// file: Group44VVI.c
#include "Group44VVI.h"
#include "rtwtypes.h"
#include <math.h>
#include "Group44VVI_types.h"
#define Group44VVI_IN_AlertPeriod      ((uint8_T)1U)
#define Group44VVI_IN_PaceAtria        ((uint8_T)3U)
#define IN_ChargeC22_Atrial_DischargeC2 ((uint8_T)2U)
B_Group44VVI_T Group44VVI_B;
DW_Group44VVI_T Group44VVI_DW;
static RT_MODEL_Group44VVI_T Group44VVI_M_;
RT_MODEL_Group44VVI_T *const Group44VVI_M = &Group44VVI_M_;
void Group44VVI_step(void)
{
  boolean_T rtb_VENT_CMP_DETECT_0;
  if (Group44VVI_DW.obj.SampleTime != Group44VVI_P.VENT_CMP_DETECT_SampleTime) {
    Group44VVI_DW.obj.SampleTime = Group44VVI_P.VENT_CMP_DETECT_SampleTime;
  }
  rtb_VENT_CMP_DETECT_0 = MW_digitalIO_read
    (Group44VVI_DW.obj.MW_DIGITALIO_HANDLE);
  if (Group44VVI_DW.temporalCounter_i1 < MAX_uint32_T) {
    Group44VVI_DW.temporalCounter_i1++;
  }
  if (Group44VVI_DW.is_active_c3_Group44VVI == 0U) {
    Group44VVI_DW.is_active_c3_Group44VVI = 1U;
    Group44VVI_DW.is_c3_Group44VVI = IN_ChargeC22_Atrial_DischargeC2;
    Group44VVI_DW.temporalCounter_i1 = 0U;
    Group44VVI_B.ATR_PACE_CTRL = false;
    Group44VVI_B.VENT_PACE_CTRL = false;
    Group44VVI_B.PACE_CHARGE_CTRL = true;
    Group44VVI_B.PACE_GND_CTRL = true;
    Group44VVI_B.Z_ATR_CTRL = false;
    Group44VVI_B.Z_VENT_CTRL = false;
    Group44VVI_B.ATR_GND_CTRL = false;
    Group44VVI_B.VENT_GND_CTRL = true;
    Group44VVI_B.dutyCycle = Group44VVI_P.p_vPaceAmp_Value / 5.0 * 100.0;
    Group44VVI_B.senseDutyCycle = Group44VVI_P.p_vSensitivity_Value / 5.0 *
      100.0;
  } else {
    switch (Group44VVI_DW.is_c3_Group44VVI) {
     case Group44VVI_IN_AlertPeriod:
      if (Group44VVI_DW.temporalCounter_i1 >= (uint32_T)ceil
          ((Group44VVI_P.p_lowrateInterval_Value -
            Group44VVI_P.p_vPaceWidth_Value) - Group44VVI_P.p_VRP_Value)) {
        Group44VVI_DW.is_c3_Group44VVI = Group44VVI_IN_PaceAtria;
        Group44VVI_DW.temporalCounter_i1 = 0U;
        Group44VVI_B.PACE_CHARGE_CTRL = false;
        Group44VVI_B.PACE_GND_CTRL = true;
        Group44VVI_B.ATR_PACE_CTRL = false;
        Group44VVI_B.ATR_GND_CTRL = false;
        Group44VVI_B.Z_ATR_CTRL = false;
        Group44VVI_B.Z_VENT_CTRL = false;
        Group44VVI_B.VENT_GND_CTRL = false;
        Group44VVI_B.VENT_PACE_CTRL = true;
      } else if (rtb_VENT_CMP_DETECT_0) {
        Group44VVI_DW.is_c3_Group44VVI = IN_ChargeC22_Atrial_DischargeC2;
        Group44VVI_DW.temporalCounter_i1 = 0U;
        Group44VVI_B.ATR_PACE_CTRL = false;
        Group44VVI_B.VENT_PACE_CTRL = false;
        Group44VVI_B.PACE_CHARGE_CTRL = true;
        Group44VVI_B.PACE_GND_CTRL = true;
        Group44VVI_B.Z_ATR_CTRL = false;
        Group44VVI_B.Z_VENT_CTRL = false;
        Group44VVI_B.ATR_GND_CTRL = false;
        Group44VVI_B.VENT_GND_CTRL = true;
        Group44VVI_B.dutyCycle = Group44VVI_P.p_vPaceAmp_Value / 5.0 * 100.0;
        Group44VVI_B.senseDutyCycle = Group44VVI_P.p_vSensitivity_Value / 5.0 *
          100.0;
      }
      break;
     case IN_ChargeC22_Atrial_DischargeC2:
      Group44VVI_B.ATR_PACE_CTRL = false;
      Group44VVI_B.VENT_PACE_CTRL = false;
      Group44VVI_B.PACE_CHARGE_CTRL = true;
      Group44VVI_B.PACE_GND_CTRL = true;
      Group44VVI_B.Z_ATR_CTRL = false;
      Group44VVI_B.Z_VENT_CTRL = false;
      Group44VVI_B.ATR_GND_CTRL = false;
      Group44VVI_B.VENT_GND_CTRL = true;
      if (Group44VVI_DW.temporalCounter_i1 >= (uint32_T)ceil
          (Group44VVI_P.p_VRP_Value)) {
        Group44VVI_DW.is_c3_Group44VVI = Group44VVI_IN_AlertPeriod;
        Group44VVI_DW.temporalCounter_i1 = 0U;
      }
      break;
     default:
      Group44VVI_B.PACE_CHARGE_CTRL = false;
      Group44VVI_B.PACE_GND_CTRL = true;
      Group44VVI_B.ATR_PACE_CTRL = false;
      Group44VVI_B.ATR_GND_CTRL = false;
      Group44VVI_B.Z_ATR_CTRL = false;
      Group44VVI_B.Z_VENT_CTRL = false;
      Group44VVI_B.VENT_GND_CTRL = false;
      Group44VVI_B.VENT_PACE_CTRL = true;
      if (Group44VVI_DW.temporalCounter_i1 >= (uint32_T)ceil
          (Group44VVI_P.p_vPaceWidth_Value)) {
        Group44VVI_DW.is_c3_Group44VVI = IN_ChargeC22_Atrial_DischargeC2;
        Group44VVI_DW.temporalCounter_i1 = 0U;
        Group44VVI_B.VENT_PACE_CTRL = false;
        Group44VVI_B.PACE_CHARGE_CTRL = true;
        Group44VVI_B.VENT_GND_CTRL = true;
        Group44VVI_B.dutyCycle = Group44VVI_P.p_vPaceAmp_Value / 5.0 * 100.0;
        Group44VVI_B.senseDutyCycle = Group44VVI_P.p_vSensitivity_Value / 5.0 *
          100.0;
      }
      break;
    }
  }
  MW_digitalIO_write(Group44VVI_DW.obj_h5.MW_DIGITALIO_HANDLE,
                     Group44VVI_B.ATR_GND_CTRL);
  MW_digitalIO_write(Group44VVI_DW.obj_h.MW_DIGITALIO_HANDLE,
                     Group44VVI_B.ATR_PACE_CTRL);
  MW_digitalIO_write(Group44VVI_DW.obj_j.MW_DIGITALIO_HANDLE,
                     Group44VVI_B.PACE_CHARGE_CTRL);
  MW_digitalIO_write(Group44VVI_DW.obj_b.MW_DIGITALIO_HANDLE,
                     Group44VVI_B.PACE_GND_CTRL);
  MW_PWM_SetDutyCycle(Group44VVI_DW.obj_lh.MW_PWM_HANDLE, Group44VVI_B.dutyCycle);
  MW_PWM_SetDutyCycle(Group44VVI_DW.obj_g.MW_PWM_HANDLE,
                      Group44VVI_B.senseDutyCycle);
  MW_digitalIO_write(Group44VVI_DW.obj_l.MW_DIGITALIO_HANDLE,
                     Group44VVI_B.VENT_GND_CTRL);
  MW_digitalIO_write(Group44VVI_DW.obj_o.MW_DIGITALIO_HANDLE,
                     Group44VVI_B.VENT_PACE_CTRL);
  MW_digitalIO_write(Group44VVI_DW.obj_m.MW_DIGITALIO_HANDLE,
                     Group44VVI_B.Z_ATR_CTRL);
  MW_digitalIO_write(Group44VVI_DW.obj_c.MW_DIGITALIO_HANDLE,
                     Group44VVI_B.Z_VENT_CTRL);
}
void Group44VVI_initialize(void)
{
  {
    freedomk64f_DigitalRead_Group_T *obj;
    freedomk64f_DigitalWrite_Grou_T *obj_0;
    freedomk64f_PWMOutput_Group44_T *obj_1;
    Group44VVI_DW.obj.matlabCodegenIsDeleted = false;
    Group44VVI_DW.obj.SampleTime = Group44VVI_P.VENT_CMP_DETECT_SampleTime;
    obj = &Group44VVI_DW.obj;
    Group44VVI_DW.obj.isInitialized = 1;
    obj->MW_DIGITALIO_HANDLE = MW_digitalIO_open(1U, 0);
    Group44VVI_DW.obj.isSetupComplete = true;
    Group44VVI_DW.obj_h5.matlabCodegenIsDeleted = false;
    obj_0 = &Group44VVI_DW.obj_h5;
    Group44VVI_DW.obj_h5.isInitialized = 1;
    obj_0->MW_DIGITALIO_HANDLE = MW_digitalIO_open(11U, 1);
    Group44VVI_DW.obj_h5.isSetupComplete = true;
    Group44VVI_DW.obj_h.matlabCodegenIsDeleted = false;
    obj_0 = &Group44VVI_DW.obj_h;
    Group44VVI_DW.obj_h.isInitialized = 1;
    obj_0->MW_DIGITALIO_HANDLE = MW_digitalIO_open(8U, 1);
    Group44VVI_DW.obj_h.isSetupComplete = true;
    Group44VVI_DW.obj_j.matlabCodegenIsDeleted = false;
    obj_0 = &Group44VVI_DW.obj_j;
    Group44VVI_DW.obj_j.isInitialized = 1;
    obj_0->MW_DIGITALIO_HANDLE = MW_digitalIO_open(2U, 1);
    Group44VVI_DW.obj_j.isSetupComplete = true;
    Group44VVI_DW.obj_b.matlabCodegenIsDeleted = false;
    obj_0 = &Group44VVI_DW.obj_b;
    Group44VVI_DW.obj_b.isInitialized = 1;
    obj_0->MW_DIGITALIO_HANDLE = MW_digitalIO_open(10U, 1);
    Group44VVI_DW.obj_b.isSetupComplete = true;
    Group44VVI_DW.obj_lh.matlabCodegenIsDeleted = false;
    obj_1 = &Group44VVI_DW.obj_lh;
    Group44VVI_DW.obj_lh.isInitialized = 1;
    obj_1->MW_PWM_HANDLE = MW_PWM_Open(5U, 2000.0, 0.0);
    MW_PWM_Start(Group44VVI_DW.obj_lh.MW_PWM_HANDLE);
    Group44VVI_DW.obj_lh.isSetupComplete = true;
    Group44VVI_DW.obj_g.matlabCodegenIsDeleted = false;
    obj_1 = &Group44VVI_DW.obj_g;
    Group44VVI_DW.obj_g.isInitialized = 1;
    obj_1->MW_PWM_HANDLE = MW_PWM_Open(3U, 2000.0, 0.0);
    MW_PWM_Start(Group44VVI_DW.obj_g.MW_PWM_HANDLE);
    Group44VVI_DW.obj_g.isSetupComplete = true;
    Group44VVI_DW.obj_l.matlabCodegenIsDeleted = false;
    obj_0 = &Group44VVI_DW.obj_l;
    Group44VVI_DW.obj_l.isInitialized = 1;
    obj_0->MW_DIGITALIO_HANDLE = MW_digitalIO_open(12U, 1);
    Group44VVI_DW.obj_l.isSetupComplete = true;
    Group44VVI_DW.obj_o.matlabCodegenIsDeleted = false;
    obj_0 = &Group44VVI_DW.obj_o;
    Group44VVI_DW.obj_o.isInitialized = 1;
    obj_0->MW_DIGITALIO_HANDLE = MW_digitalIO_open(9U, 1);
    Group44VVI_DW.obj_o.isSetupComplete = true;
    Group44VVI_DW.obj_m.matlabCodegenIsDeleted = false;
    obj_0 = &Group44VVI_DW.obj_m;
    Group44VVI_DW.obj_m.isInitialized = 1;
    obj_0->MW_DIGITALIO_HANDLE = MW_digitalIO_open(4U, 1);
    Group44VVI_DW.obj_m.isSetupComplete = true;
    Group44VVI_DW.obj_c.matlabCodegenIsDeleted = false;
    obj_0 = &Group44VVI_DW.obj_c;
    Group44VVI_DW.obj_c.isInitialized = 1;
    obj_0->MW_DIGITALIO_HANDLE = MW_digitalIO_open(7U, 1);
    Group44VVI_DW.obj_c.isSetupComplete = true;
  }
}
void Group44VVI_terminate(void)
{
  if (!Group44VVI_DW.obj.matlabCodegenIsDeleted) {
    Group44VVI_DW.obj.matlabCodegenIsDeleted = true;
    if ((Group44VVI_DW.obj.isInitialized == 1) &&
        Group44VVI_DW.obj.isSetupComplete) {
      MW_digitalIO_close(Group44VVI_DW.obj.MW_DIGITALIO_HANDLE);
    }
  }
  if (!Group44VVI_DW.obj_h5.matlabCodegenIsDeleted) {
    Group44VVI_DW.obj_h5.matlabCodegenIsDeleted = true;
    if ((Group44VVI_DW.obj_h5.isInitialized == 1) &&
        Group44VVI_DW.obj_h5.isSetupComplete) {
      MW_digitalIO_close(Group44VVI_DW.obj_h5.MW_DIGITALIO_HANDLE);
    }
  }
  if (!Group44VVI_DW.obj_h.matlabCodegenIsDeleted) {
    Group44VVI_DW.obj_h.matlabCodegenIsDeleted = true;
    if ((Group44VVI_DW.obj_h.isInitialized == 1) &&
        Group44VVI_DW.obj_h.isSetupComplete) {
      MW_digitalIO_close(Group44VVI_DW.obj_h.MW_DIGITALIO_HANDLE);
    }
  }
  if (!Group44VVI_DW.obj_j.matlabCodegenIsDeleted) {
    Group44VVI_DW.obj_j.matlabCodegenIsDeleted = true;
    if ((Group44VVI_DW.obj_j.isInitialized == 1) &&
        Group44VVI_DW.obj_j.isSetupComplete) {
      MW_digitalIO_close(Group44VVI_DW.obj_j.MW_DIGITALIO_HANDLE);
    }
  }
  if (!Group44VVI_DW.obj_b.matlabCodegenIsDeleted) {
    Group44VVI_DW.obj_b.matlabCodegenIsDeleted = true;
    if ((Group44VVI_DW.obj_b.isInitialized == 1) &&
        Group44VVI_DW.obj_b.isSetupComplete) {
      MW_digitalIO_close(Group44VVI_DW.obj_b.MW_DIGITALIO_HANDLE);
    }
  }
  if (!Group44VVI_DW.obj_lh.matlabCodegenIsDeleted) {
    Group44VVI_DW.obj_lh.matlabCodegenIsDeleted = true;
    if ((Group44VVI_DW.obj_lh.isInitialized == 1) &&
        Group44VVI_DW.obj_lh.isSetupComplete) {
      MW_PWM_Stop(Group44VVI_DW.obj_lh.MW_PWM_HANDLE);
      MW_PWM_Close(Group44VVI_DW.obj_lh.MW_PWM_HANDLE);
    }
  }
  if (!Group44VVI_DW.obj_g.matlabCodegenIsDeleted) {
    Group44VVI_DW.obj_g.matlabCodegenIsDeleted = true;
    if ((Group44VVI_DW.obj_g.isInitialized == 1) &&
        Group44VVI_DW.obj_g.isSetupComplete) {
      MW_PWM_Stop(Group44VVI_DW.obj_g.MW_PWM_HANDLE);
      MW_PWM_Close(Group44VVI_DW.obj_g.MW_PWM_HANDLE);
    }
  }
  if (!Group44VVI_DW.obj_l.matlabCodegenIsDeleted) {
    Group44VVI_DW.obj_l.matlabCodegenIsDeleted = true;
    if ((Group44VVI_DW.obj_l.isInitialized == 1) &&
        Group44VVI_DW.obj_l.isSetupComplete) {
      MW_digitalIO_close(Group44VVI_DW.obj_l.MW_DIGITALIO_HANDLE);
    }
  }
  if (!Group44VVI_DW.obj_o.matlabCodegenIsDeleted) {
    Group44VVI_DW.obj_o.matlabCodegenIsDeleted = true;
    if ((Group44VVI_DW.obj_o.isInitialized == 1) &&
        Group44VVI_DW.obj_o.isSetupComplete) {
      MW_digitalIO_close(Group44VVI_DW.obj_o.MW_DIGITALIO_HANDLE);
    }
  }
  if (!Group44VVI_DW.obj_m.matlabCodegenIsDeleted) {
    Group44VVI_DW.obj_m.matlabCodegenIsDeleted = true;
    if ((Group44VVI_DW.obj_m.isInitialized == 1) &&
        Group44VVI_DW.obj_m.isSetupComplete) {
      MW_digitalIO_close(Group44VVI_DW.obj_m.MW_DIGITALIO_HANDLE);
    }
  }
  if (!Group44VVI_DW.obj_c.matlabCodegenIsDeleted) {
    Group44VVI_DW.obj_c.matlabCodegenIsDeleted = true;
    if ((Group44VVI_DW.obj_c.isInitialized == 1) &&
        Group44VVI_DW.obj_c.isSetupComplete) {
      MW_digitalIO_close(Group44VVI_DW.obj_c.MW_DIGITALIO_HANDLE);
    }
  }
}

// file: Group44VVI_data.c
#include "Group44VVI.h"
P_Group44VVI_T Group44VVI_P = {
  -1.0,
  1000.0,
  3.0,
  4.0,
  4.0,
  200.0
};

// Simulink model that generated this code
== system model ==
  ATR_GND_CTRL : frdmk64flib/Digital Write  <- 1: Stateflowchart#1
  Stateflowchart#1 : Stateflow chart  <- 1: p_lowrateInterval, 2: VENT_CMP_DETECT, 3: p_vSensitivity, 4: p_vPaceWidth, 5: p_vPaceAmp, 6: p_VRP
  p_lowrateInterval : Constant  Value=1000
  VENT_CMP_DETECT : frdmk64flib/Digital Read
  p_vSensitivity : Constant  Value=3
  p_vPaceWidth : Constant  Value=4
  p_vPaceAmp : Constant  Value=4
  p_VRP : Constant  Value=200
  ATR_PACE_CTRL : frdmk64flib/Digital Write  <- 1: Stateflowchart#1/2
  PACE_CHARGE_CTRL : frdmk64flib/Digital Write  <- 1: Stateflowchart#1/3
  PACE_GND_CTRL : frdmk64flib/Digital Write  <- 1: Stateflowchart#1/4
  PWMOutput#1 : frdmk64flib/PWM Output  <- 1: Stateflowchart#1/9
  PWMOutput#2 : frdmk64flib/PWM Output  <- 1: Stateflowchart#1/10
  VENT_GND_CTRL : frdmk64flib/Digital Write  <- 1: Stateflowchart#1/5
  VENT_PACE_CTRL : frdmk64flib/Digital Write  <- 1: Stateflowchart#1/6
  Z_ATR_CTRL : frdmk64flib/Digital Write  <- 1: Stateflowchart#1/7
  Z_VENT_CTRL : frdmk64flib/Digital Write  <- 1: Stateflowchart#1/8
== stateflow chart Stateflowchart#1 ==
  state ChargeC22_Atrial_DischargeC21
    entry:
    ATR_PACE_CTRL = false;
    VENT_PACE_CTRL = false;
    PACE_CHARGE_CTRL = true;
    PACE_GND_CTRL = true;
    Z_ATR_CTRL = false;
    Z_VENT_CTRL = false;
    ATR_GND_CTRL = false;
    VENT_GND_CTRL = true;
    dutyCycle=p_vPaceAmp/5.0*100
    senseDutyCycle = p_vSensitivity/5.0*100
  state PaceAtria
    entry:
    PACE_CHARGE_CTRL = false;
    PACE_GND_CTRL = true;
    ATR_PACE_CTRL = false;
    ATR_GND_CTRL = false;
    Z_ATR_CTRL = false;
    Z_VENT_CTRL = false;
    VENT_GND_CTRL = false;
    VENT_PACE_CTRL = true;
    %natPaceDetected=false;
  state AlertPeriod
  (default) -> ChargeC22_Atrial_DischargeC21
  PaceAtria -> ChargeC22_Atrial_DischargeC21 : after(p_vPaceWidth,msec)
  AlertPeriod -> PaceAtria [order 1] : after(p_lowrateInterval-p_vPaceWidth-p_VRP,msec)
  AlertPeriod -> ChargeC22_Atrial_DischargeC21 [order 2] : [VENT_CMP_DETECT == true ]
  ChargeC22_Atrial_DischargeC21 -> AlertPeriod : after(p_VRP,msec)
  data: p_lowrateInterval input; ATR_GND_CTRL output; ATR_PACE_CTRL output; PACE_CHARGE_CTRL output; PACE_GND_CTRL output; VENT_GND_CTRL output; VENT_PACE_CTRL output; Z_ATR_CTRL output; Z_VENT_CTRL output; dutyCycle output; senseDutyCycle output; VENT_CMP_DETECT input; p_vSensitivity input; p_vPaceWidth input; p_vPaceAmp input; p_VRP input
